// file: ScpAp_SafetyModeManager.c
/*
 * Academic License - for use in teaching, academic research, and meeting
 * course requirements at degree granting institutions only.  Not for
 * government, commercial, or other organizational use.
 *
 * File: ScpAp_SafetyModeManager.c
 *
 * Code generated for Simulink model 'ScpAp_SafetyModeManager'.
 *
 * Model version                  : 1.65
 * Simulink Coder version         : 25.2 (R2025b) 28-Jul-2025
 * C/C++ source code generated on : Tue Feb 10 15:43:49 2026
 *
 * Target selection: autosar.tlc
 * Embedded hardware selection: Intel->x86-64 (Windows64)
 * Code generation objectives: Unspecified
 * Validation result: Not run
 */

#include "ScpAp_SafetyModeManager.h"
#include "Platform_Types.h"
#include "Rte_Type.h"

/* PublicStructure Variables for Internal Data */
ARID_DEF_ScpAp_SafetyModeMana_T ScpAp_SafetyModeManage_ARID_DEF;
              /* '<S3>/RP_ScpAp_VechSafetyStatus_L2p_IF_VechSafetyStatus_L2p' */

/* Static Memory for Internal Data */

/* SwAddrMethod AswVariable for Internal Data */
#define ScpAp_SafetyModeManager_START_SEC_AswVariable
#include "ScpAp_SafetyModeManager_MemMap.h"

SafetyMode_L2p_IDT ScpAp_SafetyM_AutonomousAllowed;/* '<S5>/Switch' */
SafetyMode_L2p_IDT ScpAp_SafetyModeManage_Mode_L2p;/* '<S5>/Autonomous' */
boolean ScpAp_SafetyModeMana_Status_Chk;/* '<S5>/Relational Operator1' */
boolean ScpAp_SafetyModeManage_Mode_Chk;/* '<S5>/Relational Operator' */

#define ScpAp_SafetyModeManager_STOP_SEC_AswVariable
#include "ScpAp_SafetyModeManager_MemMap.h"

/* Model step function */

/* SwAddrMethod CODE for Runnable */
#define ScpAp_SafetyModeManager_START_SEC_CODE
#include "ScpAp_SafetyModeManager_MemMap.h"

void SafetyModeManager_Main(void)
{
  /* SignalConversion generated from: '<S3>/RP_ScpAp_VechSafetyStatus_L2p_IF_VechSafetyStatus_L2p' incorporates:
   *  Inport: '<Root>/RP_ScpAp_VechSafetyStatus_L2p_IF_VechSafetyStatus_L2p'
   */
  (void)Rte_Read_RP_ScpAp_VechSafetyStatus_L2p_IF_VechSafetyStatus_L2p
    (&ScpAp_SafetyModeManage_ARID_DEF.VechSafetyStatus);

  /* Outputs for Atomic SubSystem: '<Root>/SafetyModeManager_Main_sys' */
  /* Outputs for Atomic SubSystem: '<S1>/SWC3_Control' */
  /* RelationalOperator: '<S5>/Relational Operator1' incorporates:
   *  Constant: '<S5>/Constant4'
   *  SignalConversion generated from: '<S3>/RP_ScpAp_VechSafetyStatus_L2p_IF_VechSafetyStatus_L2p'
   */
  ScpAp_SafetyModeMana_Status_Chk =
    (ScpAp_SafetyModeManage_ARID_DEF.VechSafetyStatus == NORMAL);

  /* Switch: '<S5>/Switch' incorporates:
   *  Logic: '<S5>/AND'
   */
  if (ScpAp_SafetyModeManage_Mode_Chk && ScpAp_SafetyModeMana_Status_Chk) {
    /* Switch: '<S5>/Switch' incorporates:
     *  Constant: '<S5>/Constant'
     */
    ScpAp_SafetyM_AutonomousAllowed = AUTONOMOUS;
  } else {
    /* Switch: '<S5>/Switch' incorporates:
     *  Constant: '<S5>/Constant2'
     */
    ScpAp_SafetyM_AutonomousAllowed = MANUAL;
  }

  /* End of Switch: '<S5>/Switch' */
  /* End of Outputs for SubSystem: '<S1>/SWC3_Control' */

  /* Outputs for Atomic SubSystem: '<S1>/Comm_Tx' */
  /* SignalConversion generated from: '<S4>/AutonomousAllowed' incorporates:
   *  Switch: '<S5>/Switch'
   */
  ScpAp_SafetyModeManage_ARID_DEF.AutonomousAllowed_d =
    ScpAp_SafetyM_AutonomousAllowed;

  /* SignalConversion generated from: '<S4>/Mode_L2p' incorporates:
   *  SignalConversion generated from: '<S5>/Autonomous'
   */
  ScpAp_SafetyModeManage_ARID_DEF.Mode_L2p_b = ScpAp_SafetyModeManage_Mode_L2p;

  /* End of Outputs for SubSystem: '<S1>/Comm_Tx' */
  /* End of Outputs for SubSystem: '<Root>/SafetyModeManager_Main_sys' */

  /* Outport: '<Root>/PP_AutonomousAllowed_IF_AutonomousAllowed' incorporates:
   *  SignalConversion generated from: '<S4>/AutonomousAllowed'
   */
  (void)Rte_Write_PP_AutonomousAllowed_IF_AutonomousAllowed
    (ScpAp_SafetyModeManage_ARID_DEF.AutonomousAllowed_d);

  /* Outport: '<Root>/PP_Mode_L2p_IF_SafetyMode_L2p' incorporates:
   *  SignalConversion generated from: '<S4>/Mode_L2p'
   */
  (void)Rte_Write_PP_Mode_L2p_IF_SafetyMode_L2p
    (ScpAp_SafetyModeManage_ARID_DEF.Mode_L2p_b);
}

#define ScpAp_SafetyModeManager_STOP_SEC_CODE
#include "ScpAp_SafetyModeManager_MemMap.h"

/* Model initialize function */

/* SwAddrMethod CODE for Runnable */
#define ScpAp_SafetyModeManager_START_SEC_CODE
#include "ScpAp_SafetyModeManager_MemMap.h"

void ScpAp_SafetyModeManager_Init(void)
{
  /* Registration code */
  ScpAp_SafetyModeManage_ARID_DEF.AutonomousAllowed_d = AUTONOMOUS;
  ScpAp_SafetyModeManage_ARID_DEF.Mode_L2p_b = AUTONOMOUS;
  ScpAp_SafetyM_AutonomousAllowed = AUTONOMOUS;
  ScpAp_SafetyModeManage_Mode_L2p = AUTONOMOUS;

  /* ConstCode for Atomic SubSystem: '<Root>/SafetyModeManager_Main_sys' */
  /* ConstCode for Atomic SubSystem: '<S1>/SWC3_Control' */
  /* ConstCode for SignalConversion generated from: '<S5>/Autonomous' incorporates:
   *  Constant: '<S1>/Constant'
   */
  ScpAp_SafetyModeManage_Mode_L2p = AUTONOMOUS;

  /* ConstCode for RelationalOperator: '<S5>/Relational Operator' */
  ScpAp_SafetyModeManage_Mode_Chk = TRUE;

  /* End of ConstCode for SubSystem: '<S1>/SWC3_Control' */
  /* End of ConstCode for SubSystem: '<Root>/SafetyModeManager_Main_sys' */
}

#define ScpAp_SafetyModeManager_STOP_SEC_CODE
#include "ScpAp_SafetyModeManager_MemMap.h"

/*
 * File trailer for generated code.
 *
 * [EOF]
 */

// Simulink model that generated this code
simulink model "ScpAp_SafetyModeManager"  (R2025b)
settings: Solver=FixedStepDiscrete  StartTime=0.0  StopTime=10.0  FixedStep=0.02  RelTol=1e-3
undefined symbols (not defined in the file): SafetyMode_L2p_IDT, VechSafetyStatus_L2p_IDT

== system ScpAp_SafetyModeManager ==
  RP_ScpAp_VechSafetyStatus_L2p_IF_VechSafetyStatus_L2p : Inport  OutDataTypeStr=Enum: VechSafetyStatus_L2p_IDT  PortDimensions=1
  SafetyModeManager_Main_sys : Subsystem  TreatAsAtomicUnit=on  SystemSampleTime=0.02
  ScpAp_SafetyModeManager_Init : Subsystem
  PP_AutonomousAllowed_IF_AutonomousAllowed : Outport  OutDataTypeStr=Enum: SafetyMode_L2p_IDT  PortDimensions=1
  PP_Mode_L2p_IF_SafetyMode_L2p : Outport  Port=2  OutDataTypeStr=Enum: SafetyMode_L2p_IDT  PortDimensions=1
  wires:
  SafetyModeManager_Main_sys/1(PP_AutonomousAllowed_IF_AutonomousAllowed) -> PP_AutonomousAllowed_IF_AutonomousAllowed/1
  SafetyModeManager_Main_sys/2(PP_Mode_L2p_IF_SafetyMode_L2p) -> PP_Mode_L2p_IF_SafetyMode_L2p/1
  RP_ScpAp_VechSafetyStatus_L2p_IF_VechSafetyStatus_L2p/1 -> SafetyModeManager_Main_sys/1(RP_ScpAp_VechSafetyStatus_L2p_IF_VechSafetyStatus_L2p)

== system ScpAp_SafetyModeManager/SafetyModeManager_Main_sys ==
  RP_ScpAp_VechSafetyStatus_L2p_IF_VechSafetyStatus_L2p : Inport  OutDataTypeStr=Enum: VechSafetyStatus_L2p_IDT  PortDimensions=1
  Comm_Rx : Subsystem
  Comm_Tx : Subsystem
  Constant : Constant  Value=SafetyMode_L2p_IDT.AUTONOMOUS
  SWC3_Control : Subsystem  TreatAsAtomicUnit=on
  PP_AutonomousAllowed_IF_AutonomousAllowed : Outport
  PP_Mode_L2p_IF_SafetyMode_L2p : Outport  Port=2
  wires:
  RP_ScpAp_VechSafetyStatus_L2p_IF_VechSafetyStatus_L2p/1 -> Comm_Rx/1(RP_ScpAp_VechSafetyStatus_L2p_IF_VechSafetyStatus_L2p)
  Comm_Rx/1(VechSafetyStatus) -> [VechSafetyStatus]
  SWC3_Control/1(AutonomousAllowed) -> [AutonomousAllowed]
  [Mode_L2p] -> Comm_Tx/2(Mode_L2p)
  [AutonomousAllowed] -> Comm_Tx/1(AutonomousAllowed)
  Comm_Tx/1(PP_AutonomousAllowed_IF_AutonomousAllowed) -> PP_AutonomousAllowed_IF_AutonomousAllowed/1
  Comm_Tx/2(PP_Mode_L2p_IF_SafetyMode_L2p) -> PP_Mode_L2p_IF_SafetyMode_L2p/1
  Constant/1 -> SWC3_Control/1(Autonomous)  "Mode_L2p"
  [VechSafetyStatus] -> SWC3_Control/2(VechSafetyStatus)
  SWC3_Control/2(Mode_L2p) -> [Mode_L2p]

== system ScpAp_SafetyModeManager/ScpAp_SafetyModeManager_Init ==
  Event Listener : EventListener  EventName=reset

== system ScpAp_SafetyModeManager/SafetyModeManager_Main_sys/Comm_Rx ==
  RP_ScpAp_VechSafetyStatus_L2p_IF_VechSafetyStatus_L2p : Inport  OutDataTypeStr=Enum: VechSafetyStatus_L2p_IDT
  Data Type Conversion : DataTypeConversion  OutDataTypeStr=Enum: VechSafetyStatus_L2p_IDT  SaturateOnIntegerOverflow=off  RndMeth=Floor
  VechSafetyStatus : Outport
  wires:
  RP_ScpAp_VechSafetyStatus_L2p_IF_VechSafetyStatus_L2p/1 -> Data Type Conversion/1
  Data Type Conversion/1 -> VechSafetyStatus/1  "VechSafetyStatus"

== system ScpAp_SafetyModeManager/SafetyModeManager_Main_sys/Comm_Tx ==
  AutonomousAllowed : Inport  OutDataTypeStr=Enum: SafetyMode_L2p_IDT
  Mode_L2p : Inport  Port=2
  PP_AutonomousAllowed_IF_AutonomousAllowed : Outport  OutDataTypeStr=Enum: SafetyMode_L2p_IDT
  PP_Mode_L2p_IF_SafetyMode_L2p : Outport  Port=2
  wires:
  Mode_L2p/1 -> PP_Mode_L2p_IF_SafetyMode_L2p/1  "Mode_L2p"
  AutonomousAllowed/1 -> PP_AutonomousAllowed_IF_AutonomousAllowed/1  "AutonomousAllowed"

== system ScpAp_SafetyModeManager/SafetyModeManager_Main_sys/SWC3_Control ==
  Autonomous : Inport
  VechSafetyStatus : Inport  Port=2  OutDataTypeStr=Enum: VechSafetyStatus_L2p_IDT
  AND : Logic  AllPortsSameDT=off  OutDataTypeStr=boolean
  Constant : Constant  Value=SafetyMode_L2p_IDT.AUTONOMOUS  OutDataTypeStr=Enum: SafetyMode_L2p_IDT
  Constant1 : Constant  Value=SafetyMode_L2p_IDT.AUTONOMOUS  OutDataTypeStr=Enum: SafetyMode_L2p_IDT
  Constant2 : Constant  Value=SafetyMode_L2p_IDT.MANUAL  OutDataTypeStr=Enum: SafetyMode_L2p_IDT
  Constant4 : Constant  Value=VechSafetyStatus_L2p_IDT.NORMAL  OutDataTypeStr=Enum: VechSafetyStatus_L2p_IDT
  Relational Operator : RelationalOperator  Operator===  OutDataTypeStr=boolean  RndMeth=Simplest  InputSameDT=off
  Relational Operator1 : RelationalOperator  Operator===  OutDataTypeStr=boolean  RndMeth=Simplest  InputSameDT=off
  Switch : Switch  Criteria=u2 > Threshold  SaturateOnIntegerOverflow=off  InputSameDT=off
  AutonomousAllowed : Outport  OutDataTypeStr=Enum: SafetyMode_L2p_IDT
  Mode_L2p : Outport  Port=2
  wires:
  Constant1/1 -> Relational Operator/2
  Relational Operator/1 -> AND/1  "Mode_Chk"
  AND/1 -> Switch/2  "AutonomousAllowed_Chk"
  Constant4/1 -> Relational Operator1/2
  Relational Operator1/1 -> AND/2  "Status_Chk"
  Autonomous/1 -> [Mode_L2p]
  [Mode_L2p] -> Mode_L2p/1  "Mode_L2p"
  Switch/1 -> AutonomousAllowed/1  "AutonomousAllowed"
  Constant/1 -> Switch/1
  Constant2/1 -> Switch/3
  [Mode_L2p] -> Relational Operator/1
  VechSafetyStatus/1 -> Relational Operator1/1
